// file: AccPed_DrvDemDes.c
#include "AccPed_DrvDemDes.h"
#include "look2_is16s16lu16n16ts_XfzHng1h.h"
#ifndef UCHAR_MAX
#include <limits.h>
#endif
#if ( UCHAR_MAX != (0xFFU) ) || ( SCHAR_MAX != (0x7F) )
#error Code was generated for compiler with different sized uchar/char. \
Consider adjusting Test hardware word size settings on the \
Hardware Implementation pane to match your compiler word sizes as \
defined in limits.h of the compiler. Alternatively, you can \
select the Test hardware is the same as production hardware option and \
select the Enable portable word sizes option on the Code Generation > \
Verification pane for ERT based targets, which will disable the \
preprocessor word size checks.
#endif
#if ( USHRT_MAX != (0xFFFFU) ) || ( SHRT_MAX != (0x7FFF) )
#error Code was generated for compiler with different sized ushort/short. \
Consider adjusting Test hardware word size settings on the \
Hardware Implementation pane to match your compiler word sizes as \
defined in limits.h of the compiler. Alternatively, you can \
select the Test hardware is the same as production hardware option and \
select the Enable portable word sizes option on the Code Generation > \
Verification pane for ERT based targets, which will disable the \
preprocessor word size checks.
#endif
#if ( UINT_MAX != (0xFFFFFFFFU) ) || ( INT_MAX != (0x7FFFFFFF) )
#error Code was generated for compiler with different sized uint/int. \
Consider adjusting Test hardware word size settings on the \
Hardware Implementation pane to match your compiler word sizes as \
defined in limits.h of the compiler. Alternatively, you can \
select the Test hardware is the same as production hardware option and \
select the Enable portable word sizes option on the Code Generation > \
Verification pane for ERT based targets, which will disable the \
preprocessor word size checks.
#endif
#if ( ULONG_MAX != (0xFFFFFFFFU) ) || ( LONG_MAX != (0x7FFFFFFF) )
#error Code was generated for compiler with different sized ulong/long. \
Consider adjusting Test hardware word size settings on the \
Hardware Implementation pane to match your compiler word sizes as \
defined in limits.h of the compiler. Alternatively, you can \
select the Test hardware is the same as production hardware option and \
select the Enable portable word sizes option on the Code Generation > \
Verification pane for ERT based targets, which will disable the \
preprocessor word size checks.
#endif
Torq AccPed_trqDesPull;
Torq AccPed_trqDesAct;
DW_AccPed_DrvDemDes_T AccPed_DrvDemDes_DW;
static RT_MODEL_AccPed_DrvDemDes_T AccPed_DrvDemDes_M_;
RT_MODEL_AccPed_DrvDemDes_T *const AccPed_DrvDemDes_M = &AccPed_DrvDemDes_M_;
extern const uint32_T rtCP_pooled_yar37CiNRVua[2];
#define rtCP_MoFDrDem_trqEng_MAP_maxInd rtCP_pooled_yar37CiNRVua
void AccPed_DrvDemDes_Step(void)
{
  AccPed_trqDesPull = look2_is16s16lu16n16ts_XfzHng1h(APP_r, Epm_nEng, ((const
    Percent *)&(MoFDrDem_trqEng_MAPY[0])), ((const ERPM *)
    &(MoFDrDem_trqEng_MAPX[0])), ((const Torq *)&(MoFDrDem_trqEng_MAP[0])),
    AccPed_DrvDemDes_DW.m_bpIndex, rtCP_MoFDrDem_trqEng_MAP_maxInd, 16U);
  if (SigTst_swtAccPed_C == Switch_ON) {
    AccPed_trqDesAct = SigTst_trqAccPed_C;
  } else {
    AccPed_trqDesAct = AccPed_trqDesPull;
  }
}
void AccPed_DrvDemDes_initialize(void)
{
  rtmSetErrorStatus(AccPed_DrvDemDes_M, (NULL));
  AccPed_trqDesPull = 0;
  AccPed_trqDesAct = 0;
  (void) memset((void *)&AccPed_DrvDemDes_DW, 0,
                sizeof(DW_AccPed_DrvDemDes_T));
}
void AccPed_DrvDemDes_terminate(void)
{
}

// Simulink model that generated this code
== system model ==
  AccPed_DrvDemDes_Step : Inport
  APP_r : Inport
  Epm_nEng : Inport
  AccPed_trqDesAct : Outport  <- 1: AccPed_DrvDemDes
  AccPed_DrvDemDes : Subsystem  <- 1: APP_r, 2: Epm_nEng, Trigger: AccPed_DrvDemDes_Step
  AccPed_trqDesPull : Outport  <- 1: AccPed_DrvDemDes/2
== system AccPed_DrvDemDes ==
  Inport#1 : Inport
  Inport#2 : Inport
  TriggerPort#1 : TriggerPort  TriggerType=function-call
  Outport#1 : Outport  <- 1: Switch
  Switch : Switch  Criteria=u2 ~= 0  <- 1: Constant#1, 2: RelationalOperator#1, 3: MoFDrDem_trqEng_MAP
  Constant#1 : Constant  Value=SigTst_trqAccPed_C
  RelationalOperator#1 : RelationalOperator  Operator===  <- 1: Constant#2, 2: Constant#3
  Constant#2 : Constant  Value=SigTst_swtAccPed_C
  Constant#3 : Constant  Value=Switch.ON
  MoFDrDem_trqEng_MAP : Lookup_n-D  BreakpointsForDimension1=MoFDrDem_trqEng_MAPY  BreakpointsForDimension2=MoFDrDem_trqEng_MAPX  Table=MoFDrDem_trqEng_MAP  <- 1: Inport#1, 2: Inport#2
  Outport#2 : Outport  <- 1: MoFDrDem_trqEng_MAP
